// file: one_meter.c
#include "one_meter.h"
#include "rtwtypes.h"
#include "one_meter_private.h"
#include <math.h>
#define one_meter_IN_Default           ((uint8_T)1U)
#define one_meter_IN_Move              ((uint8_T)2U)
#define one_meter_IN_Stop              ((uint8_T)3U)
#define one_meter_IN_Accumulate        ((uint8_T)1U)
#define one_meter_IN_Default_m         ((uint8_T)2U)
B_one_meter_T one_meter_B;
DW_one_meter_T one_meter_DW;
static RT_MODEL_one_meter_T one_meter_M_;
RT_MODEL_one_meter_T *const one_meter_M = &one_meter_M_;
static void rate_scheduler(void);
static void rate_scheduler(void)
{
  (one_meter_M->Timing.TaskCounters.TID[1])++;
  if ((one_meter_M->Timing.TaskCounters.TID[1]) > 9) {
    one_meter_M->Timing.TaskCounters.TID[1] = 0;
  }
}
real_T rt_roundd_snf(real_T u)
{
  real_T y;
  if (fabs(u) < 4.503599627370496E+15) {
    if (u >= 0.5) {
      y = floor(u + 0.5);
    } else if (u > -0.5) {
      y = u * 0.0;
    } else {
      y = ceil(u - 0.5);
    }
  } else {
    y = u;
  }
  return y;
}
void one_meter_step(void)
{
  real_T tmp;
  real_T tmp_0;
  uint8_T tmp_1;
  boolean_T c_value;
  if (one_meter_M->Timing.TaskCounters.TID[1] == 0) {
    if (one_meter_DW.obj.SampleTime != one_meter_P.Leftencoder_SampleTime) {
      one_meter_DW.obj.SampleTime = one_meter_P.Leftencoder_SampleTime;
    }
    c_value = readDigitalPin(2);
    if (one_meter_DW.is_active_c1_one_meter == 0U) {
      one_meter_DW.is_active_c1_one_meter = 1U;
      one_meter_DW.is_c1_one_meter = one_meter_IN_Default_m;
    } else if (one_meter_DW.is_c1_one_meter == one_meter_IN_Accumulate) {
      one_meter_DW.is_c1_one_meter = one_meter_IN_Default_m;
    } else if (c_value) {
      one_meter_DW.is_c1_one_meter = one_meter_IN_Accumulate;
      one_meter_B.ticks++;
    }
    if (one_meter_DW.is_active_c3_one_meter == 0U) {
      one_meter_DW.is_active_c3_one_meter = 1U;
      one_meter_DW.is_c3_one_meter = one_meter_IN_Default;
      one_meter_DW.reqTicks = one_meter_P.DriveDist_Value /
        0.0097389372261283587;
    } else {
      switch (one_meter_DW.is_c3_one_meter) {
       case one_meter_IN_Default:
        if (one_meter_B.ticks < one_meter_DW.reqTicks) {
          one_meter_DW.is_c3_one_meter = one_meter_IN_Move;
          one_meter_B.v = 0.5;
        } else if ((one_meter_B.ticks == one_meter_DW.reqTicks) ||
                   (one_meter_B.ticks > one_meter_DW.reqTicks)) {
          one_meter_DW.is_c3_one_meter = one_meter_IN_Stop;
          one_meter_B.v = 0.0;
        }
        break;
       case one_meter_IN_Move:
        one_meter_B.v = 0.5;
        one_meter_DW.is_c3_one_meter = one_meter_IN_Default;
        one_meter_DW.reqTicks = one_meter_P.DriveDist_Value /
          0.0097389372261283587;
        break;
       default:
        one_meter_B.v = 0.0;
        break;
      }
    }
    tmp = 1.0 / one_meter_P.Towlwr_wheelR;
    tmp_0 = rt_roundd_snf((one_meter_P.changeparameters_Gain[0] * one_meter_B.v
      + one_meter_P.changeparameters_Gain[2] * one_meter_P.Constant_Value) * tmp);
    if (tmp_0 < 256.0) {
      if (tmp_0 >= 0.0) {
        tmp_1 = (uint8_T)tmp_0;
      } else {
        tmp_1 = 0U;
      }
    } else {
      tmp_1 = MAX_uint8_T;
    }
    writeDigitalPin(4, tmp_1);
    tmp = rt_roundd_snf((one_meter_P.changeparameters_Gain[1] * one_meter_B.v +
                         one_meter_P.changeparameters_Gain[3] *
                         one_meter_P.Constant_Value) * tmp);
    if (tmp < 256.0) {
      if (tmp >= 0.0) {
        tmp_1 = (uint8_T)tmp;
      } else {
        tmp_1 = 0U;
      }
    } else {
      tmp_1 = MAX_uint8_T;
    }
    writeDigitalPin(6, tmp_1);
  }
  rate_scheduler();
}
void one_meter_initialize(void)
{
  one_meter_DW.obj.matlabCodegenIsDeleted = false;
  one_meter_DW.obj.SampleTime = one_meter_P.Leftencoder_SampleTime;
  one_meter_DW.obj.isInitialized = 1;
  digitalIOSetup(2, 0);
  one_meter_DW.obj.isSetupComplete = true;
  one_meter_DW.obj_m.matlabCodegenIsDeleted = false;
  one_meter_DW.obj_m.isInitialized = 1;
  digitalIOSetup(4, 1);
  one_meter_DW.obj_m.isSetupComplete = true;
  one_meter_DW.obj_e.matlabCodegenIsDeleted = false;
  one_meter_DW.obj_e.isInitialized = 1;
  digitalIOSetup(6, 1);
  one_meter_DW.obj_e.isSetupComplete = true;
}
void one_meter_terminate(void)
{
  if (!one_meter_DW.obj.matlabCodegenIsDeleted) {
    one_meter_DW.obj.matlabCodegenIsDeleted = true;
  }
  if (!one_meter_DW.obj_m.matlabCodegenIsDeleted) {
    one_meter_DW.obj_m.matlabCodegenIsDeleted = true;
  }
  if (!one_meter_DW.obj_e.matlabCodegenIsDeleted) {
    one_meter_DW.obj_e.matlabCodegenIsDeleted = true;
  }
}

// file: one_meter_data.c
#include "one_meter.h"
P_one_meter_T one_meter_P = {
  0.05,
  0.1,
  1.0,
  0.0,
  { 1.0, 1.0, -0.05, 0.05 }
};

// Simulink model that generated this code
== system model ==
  DigitalOutput#1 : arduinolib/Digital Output  pinNumber=4  <- 1: Towlwr
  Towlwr : mobileRoboticsTrainingLib/To wlwr  <- 1: Stateflowchart#1, 2: Constant
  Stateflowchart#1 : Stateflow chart  <- 1: DriveDist, 2: Stateflowchart#2
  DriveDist : Constant
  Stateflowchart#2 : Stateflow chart  <- 1: Leftencoder
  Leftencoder : arduinolib/Digital Input  pinNumber=2
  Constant : Constant  Value=0
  DigitalOutput#2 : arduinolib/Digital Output  pinNumber=6  <- 1: Towlwr/2
== stateflow chart Stateflowchart#2 ==
  state Default
    entry:
    LeftEncoderTicks;
    ticks;
  state Accumulate
    entry:
    ticks = ticks + 1;
  (default) -> Default
  Accumulate -> Default
  Default -> Accumulate : [LeftEncoderTicks == 1]
  data: ticks output =0; LeftEncoderTicks input

== stateflow chart Stateflowchart#1 ==
  state Default
    entry:
    ticks;
    dist1Tick=(pi*0.031)/10
    reqTicks=reqDist/dist1Tick;
  state Stop
    entry:
    v=0;
  state Move
    entry:
    v=0.5;
  (default) -> Default
  Default -> Stop [order 2] : [ticks==reqTicks | ticks>reqTicks]
  Move -> Default
  Default -> Move [order 1] : [ticks<reqTicks]
  data: reqDist input; ticks input; v output; dist1Tick local; reqTicks local
